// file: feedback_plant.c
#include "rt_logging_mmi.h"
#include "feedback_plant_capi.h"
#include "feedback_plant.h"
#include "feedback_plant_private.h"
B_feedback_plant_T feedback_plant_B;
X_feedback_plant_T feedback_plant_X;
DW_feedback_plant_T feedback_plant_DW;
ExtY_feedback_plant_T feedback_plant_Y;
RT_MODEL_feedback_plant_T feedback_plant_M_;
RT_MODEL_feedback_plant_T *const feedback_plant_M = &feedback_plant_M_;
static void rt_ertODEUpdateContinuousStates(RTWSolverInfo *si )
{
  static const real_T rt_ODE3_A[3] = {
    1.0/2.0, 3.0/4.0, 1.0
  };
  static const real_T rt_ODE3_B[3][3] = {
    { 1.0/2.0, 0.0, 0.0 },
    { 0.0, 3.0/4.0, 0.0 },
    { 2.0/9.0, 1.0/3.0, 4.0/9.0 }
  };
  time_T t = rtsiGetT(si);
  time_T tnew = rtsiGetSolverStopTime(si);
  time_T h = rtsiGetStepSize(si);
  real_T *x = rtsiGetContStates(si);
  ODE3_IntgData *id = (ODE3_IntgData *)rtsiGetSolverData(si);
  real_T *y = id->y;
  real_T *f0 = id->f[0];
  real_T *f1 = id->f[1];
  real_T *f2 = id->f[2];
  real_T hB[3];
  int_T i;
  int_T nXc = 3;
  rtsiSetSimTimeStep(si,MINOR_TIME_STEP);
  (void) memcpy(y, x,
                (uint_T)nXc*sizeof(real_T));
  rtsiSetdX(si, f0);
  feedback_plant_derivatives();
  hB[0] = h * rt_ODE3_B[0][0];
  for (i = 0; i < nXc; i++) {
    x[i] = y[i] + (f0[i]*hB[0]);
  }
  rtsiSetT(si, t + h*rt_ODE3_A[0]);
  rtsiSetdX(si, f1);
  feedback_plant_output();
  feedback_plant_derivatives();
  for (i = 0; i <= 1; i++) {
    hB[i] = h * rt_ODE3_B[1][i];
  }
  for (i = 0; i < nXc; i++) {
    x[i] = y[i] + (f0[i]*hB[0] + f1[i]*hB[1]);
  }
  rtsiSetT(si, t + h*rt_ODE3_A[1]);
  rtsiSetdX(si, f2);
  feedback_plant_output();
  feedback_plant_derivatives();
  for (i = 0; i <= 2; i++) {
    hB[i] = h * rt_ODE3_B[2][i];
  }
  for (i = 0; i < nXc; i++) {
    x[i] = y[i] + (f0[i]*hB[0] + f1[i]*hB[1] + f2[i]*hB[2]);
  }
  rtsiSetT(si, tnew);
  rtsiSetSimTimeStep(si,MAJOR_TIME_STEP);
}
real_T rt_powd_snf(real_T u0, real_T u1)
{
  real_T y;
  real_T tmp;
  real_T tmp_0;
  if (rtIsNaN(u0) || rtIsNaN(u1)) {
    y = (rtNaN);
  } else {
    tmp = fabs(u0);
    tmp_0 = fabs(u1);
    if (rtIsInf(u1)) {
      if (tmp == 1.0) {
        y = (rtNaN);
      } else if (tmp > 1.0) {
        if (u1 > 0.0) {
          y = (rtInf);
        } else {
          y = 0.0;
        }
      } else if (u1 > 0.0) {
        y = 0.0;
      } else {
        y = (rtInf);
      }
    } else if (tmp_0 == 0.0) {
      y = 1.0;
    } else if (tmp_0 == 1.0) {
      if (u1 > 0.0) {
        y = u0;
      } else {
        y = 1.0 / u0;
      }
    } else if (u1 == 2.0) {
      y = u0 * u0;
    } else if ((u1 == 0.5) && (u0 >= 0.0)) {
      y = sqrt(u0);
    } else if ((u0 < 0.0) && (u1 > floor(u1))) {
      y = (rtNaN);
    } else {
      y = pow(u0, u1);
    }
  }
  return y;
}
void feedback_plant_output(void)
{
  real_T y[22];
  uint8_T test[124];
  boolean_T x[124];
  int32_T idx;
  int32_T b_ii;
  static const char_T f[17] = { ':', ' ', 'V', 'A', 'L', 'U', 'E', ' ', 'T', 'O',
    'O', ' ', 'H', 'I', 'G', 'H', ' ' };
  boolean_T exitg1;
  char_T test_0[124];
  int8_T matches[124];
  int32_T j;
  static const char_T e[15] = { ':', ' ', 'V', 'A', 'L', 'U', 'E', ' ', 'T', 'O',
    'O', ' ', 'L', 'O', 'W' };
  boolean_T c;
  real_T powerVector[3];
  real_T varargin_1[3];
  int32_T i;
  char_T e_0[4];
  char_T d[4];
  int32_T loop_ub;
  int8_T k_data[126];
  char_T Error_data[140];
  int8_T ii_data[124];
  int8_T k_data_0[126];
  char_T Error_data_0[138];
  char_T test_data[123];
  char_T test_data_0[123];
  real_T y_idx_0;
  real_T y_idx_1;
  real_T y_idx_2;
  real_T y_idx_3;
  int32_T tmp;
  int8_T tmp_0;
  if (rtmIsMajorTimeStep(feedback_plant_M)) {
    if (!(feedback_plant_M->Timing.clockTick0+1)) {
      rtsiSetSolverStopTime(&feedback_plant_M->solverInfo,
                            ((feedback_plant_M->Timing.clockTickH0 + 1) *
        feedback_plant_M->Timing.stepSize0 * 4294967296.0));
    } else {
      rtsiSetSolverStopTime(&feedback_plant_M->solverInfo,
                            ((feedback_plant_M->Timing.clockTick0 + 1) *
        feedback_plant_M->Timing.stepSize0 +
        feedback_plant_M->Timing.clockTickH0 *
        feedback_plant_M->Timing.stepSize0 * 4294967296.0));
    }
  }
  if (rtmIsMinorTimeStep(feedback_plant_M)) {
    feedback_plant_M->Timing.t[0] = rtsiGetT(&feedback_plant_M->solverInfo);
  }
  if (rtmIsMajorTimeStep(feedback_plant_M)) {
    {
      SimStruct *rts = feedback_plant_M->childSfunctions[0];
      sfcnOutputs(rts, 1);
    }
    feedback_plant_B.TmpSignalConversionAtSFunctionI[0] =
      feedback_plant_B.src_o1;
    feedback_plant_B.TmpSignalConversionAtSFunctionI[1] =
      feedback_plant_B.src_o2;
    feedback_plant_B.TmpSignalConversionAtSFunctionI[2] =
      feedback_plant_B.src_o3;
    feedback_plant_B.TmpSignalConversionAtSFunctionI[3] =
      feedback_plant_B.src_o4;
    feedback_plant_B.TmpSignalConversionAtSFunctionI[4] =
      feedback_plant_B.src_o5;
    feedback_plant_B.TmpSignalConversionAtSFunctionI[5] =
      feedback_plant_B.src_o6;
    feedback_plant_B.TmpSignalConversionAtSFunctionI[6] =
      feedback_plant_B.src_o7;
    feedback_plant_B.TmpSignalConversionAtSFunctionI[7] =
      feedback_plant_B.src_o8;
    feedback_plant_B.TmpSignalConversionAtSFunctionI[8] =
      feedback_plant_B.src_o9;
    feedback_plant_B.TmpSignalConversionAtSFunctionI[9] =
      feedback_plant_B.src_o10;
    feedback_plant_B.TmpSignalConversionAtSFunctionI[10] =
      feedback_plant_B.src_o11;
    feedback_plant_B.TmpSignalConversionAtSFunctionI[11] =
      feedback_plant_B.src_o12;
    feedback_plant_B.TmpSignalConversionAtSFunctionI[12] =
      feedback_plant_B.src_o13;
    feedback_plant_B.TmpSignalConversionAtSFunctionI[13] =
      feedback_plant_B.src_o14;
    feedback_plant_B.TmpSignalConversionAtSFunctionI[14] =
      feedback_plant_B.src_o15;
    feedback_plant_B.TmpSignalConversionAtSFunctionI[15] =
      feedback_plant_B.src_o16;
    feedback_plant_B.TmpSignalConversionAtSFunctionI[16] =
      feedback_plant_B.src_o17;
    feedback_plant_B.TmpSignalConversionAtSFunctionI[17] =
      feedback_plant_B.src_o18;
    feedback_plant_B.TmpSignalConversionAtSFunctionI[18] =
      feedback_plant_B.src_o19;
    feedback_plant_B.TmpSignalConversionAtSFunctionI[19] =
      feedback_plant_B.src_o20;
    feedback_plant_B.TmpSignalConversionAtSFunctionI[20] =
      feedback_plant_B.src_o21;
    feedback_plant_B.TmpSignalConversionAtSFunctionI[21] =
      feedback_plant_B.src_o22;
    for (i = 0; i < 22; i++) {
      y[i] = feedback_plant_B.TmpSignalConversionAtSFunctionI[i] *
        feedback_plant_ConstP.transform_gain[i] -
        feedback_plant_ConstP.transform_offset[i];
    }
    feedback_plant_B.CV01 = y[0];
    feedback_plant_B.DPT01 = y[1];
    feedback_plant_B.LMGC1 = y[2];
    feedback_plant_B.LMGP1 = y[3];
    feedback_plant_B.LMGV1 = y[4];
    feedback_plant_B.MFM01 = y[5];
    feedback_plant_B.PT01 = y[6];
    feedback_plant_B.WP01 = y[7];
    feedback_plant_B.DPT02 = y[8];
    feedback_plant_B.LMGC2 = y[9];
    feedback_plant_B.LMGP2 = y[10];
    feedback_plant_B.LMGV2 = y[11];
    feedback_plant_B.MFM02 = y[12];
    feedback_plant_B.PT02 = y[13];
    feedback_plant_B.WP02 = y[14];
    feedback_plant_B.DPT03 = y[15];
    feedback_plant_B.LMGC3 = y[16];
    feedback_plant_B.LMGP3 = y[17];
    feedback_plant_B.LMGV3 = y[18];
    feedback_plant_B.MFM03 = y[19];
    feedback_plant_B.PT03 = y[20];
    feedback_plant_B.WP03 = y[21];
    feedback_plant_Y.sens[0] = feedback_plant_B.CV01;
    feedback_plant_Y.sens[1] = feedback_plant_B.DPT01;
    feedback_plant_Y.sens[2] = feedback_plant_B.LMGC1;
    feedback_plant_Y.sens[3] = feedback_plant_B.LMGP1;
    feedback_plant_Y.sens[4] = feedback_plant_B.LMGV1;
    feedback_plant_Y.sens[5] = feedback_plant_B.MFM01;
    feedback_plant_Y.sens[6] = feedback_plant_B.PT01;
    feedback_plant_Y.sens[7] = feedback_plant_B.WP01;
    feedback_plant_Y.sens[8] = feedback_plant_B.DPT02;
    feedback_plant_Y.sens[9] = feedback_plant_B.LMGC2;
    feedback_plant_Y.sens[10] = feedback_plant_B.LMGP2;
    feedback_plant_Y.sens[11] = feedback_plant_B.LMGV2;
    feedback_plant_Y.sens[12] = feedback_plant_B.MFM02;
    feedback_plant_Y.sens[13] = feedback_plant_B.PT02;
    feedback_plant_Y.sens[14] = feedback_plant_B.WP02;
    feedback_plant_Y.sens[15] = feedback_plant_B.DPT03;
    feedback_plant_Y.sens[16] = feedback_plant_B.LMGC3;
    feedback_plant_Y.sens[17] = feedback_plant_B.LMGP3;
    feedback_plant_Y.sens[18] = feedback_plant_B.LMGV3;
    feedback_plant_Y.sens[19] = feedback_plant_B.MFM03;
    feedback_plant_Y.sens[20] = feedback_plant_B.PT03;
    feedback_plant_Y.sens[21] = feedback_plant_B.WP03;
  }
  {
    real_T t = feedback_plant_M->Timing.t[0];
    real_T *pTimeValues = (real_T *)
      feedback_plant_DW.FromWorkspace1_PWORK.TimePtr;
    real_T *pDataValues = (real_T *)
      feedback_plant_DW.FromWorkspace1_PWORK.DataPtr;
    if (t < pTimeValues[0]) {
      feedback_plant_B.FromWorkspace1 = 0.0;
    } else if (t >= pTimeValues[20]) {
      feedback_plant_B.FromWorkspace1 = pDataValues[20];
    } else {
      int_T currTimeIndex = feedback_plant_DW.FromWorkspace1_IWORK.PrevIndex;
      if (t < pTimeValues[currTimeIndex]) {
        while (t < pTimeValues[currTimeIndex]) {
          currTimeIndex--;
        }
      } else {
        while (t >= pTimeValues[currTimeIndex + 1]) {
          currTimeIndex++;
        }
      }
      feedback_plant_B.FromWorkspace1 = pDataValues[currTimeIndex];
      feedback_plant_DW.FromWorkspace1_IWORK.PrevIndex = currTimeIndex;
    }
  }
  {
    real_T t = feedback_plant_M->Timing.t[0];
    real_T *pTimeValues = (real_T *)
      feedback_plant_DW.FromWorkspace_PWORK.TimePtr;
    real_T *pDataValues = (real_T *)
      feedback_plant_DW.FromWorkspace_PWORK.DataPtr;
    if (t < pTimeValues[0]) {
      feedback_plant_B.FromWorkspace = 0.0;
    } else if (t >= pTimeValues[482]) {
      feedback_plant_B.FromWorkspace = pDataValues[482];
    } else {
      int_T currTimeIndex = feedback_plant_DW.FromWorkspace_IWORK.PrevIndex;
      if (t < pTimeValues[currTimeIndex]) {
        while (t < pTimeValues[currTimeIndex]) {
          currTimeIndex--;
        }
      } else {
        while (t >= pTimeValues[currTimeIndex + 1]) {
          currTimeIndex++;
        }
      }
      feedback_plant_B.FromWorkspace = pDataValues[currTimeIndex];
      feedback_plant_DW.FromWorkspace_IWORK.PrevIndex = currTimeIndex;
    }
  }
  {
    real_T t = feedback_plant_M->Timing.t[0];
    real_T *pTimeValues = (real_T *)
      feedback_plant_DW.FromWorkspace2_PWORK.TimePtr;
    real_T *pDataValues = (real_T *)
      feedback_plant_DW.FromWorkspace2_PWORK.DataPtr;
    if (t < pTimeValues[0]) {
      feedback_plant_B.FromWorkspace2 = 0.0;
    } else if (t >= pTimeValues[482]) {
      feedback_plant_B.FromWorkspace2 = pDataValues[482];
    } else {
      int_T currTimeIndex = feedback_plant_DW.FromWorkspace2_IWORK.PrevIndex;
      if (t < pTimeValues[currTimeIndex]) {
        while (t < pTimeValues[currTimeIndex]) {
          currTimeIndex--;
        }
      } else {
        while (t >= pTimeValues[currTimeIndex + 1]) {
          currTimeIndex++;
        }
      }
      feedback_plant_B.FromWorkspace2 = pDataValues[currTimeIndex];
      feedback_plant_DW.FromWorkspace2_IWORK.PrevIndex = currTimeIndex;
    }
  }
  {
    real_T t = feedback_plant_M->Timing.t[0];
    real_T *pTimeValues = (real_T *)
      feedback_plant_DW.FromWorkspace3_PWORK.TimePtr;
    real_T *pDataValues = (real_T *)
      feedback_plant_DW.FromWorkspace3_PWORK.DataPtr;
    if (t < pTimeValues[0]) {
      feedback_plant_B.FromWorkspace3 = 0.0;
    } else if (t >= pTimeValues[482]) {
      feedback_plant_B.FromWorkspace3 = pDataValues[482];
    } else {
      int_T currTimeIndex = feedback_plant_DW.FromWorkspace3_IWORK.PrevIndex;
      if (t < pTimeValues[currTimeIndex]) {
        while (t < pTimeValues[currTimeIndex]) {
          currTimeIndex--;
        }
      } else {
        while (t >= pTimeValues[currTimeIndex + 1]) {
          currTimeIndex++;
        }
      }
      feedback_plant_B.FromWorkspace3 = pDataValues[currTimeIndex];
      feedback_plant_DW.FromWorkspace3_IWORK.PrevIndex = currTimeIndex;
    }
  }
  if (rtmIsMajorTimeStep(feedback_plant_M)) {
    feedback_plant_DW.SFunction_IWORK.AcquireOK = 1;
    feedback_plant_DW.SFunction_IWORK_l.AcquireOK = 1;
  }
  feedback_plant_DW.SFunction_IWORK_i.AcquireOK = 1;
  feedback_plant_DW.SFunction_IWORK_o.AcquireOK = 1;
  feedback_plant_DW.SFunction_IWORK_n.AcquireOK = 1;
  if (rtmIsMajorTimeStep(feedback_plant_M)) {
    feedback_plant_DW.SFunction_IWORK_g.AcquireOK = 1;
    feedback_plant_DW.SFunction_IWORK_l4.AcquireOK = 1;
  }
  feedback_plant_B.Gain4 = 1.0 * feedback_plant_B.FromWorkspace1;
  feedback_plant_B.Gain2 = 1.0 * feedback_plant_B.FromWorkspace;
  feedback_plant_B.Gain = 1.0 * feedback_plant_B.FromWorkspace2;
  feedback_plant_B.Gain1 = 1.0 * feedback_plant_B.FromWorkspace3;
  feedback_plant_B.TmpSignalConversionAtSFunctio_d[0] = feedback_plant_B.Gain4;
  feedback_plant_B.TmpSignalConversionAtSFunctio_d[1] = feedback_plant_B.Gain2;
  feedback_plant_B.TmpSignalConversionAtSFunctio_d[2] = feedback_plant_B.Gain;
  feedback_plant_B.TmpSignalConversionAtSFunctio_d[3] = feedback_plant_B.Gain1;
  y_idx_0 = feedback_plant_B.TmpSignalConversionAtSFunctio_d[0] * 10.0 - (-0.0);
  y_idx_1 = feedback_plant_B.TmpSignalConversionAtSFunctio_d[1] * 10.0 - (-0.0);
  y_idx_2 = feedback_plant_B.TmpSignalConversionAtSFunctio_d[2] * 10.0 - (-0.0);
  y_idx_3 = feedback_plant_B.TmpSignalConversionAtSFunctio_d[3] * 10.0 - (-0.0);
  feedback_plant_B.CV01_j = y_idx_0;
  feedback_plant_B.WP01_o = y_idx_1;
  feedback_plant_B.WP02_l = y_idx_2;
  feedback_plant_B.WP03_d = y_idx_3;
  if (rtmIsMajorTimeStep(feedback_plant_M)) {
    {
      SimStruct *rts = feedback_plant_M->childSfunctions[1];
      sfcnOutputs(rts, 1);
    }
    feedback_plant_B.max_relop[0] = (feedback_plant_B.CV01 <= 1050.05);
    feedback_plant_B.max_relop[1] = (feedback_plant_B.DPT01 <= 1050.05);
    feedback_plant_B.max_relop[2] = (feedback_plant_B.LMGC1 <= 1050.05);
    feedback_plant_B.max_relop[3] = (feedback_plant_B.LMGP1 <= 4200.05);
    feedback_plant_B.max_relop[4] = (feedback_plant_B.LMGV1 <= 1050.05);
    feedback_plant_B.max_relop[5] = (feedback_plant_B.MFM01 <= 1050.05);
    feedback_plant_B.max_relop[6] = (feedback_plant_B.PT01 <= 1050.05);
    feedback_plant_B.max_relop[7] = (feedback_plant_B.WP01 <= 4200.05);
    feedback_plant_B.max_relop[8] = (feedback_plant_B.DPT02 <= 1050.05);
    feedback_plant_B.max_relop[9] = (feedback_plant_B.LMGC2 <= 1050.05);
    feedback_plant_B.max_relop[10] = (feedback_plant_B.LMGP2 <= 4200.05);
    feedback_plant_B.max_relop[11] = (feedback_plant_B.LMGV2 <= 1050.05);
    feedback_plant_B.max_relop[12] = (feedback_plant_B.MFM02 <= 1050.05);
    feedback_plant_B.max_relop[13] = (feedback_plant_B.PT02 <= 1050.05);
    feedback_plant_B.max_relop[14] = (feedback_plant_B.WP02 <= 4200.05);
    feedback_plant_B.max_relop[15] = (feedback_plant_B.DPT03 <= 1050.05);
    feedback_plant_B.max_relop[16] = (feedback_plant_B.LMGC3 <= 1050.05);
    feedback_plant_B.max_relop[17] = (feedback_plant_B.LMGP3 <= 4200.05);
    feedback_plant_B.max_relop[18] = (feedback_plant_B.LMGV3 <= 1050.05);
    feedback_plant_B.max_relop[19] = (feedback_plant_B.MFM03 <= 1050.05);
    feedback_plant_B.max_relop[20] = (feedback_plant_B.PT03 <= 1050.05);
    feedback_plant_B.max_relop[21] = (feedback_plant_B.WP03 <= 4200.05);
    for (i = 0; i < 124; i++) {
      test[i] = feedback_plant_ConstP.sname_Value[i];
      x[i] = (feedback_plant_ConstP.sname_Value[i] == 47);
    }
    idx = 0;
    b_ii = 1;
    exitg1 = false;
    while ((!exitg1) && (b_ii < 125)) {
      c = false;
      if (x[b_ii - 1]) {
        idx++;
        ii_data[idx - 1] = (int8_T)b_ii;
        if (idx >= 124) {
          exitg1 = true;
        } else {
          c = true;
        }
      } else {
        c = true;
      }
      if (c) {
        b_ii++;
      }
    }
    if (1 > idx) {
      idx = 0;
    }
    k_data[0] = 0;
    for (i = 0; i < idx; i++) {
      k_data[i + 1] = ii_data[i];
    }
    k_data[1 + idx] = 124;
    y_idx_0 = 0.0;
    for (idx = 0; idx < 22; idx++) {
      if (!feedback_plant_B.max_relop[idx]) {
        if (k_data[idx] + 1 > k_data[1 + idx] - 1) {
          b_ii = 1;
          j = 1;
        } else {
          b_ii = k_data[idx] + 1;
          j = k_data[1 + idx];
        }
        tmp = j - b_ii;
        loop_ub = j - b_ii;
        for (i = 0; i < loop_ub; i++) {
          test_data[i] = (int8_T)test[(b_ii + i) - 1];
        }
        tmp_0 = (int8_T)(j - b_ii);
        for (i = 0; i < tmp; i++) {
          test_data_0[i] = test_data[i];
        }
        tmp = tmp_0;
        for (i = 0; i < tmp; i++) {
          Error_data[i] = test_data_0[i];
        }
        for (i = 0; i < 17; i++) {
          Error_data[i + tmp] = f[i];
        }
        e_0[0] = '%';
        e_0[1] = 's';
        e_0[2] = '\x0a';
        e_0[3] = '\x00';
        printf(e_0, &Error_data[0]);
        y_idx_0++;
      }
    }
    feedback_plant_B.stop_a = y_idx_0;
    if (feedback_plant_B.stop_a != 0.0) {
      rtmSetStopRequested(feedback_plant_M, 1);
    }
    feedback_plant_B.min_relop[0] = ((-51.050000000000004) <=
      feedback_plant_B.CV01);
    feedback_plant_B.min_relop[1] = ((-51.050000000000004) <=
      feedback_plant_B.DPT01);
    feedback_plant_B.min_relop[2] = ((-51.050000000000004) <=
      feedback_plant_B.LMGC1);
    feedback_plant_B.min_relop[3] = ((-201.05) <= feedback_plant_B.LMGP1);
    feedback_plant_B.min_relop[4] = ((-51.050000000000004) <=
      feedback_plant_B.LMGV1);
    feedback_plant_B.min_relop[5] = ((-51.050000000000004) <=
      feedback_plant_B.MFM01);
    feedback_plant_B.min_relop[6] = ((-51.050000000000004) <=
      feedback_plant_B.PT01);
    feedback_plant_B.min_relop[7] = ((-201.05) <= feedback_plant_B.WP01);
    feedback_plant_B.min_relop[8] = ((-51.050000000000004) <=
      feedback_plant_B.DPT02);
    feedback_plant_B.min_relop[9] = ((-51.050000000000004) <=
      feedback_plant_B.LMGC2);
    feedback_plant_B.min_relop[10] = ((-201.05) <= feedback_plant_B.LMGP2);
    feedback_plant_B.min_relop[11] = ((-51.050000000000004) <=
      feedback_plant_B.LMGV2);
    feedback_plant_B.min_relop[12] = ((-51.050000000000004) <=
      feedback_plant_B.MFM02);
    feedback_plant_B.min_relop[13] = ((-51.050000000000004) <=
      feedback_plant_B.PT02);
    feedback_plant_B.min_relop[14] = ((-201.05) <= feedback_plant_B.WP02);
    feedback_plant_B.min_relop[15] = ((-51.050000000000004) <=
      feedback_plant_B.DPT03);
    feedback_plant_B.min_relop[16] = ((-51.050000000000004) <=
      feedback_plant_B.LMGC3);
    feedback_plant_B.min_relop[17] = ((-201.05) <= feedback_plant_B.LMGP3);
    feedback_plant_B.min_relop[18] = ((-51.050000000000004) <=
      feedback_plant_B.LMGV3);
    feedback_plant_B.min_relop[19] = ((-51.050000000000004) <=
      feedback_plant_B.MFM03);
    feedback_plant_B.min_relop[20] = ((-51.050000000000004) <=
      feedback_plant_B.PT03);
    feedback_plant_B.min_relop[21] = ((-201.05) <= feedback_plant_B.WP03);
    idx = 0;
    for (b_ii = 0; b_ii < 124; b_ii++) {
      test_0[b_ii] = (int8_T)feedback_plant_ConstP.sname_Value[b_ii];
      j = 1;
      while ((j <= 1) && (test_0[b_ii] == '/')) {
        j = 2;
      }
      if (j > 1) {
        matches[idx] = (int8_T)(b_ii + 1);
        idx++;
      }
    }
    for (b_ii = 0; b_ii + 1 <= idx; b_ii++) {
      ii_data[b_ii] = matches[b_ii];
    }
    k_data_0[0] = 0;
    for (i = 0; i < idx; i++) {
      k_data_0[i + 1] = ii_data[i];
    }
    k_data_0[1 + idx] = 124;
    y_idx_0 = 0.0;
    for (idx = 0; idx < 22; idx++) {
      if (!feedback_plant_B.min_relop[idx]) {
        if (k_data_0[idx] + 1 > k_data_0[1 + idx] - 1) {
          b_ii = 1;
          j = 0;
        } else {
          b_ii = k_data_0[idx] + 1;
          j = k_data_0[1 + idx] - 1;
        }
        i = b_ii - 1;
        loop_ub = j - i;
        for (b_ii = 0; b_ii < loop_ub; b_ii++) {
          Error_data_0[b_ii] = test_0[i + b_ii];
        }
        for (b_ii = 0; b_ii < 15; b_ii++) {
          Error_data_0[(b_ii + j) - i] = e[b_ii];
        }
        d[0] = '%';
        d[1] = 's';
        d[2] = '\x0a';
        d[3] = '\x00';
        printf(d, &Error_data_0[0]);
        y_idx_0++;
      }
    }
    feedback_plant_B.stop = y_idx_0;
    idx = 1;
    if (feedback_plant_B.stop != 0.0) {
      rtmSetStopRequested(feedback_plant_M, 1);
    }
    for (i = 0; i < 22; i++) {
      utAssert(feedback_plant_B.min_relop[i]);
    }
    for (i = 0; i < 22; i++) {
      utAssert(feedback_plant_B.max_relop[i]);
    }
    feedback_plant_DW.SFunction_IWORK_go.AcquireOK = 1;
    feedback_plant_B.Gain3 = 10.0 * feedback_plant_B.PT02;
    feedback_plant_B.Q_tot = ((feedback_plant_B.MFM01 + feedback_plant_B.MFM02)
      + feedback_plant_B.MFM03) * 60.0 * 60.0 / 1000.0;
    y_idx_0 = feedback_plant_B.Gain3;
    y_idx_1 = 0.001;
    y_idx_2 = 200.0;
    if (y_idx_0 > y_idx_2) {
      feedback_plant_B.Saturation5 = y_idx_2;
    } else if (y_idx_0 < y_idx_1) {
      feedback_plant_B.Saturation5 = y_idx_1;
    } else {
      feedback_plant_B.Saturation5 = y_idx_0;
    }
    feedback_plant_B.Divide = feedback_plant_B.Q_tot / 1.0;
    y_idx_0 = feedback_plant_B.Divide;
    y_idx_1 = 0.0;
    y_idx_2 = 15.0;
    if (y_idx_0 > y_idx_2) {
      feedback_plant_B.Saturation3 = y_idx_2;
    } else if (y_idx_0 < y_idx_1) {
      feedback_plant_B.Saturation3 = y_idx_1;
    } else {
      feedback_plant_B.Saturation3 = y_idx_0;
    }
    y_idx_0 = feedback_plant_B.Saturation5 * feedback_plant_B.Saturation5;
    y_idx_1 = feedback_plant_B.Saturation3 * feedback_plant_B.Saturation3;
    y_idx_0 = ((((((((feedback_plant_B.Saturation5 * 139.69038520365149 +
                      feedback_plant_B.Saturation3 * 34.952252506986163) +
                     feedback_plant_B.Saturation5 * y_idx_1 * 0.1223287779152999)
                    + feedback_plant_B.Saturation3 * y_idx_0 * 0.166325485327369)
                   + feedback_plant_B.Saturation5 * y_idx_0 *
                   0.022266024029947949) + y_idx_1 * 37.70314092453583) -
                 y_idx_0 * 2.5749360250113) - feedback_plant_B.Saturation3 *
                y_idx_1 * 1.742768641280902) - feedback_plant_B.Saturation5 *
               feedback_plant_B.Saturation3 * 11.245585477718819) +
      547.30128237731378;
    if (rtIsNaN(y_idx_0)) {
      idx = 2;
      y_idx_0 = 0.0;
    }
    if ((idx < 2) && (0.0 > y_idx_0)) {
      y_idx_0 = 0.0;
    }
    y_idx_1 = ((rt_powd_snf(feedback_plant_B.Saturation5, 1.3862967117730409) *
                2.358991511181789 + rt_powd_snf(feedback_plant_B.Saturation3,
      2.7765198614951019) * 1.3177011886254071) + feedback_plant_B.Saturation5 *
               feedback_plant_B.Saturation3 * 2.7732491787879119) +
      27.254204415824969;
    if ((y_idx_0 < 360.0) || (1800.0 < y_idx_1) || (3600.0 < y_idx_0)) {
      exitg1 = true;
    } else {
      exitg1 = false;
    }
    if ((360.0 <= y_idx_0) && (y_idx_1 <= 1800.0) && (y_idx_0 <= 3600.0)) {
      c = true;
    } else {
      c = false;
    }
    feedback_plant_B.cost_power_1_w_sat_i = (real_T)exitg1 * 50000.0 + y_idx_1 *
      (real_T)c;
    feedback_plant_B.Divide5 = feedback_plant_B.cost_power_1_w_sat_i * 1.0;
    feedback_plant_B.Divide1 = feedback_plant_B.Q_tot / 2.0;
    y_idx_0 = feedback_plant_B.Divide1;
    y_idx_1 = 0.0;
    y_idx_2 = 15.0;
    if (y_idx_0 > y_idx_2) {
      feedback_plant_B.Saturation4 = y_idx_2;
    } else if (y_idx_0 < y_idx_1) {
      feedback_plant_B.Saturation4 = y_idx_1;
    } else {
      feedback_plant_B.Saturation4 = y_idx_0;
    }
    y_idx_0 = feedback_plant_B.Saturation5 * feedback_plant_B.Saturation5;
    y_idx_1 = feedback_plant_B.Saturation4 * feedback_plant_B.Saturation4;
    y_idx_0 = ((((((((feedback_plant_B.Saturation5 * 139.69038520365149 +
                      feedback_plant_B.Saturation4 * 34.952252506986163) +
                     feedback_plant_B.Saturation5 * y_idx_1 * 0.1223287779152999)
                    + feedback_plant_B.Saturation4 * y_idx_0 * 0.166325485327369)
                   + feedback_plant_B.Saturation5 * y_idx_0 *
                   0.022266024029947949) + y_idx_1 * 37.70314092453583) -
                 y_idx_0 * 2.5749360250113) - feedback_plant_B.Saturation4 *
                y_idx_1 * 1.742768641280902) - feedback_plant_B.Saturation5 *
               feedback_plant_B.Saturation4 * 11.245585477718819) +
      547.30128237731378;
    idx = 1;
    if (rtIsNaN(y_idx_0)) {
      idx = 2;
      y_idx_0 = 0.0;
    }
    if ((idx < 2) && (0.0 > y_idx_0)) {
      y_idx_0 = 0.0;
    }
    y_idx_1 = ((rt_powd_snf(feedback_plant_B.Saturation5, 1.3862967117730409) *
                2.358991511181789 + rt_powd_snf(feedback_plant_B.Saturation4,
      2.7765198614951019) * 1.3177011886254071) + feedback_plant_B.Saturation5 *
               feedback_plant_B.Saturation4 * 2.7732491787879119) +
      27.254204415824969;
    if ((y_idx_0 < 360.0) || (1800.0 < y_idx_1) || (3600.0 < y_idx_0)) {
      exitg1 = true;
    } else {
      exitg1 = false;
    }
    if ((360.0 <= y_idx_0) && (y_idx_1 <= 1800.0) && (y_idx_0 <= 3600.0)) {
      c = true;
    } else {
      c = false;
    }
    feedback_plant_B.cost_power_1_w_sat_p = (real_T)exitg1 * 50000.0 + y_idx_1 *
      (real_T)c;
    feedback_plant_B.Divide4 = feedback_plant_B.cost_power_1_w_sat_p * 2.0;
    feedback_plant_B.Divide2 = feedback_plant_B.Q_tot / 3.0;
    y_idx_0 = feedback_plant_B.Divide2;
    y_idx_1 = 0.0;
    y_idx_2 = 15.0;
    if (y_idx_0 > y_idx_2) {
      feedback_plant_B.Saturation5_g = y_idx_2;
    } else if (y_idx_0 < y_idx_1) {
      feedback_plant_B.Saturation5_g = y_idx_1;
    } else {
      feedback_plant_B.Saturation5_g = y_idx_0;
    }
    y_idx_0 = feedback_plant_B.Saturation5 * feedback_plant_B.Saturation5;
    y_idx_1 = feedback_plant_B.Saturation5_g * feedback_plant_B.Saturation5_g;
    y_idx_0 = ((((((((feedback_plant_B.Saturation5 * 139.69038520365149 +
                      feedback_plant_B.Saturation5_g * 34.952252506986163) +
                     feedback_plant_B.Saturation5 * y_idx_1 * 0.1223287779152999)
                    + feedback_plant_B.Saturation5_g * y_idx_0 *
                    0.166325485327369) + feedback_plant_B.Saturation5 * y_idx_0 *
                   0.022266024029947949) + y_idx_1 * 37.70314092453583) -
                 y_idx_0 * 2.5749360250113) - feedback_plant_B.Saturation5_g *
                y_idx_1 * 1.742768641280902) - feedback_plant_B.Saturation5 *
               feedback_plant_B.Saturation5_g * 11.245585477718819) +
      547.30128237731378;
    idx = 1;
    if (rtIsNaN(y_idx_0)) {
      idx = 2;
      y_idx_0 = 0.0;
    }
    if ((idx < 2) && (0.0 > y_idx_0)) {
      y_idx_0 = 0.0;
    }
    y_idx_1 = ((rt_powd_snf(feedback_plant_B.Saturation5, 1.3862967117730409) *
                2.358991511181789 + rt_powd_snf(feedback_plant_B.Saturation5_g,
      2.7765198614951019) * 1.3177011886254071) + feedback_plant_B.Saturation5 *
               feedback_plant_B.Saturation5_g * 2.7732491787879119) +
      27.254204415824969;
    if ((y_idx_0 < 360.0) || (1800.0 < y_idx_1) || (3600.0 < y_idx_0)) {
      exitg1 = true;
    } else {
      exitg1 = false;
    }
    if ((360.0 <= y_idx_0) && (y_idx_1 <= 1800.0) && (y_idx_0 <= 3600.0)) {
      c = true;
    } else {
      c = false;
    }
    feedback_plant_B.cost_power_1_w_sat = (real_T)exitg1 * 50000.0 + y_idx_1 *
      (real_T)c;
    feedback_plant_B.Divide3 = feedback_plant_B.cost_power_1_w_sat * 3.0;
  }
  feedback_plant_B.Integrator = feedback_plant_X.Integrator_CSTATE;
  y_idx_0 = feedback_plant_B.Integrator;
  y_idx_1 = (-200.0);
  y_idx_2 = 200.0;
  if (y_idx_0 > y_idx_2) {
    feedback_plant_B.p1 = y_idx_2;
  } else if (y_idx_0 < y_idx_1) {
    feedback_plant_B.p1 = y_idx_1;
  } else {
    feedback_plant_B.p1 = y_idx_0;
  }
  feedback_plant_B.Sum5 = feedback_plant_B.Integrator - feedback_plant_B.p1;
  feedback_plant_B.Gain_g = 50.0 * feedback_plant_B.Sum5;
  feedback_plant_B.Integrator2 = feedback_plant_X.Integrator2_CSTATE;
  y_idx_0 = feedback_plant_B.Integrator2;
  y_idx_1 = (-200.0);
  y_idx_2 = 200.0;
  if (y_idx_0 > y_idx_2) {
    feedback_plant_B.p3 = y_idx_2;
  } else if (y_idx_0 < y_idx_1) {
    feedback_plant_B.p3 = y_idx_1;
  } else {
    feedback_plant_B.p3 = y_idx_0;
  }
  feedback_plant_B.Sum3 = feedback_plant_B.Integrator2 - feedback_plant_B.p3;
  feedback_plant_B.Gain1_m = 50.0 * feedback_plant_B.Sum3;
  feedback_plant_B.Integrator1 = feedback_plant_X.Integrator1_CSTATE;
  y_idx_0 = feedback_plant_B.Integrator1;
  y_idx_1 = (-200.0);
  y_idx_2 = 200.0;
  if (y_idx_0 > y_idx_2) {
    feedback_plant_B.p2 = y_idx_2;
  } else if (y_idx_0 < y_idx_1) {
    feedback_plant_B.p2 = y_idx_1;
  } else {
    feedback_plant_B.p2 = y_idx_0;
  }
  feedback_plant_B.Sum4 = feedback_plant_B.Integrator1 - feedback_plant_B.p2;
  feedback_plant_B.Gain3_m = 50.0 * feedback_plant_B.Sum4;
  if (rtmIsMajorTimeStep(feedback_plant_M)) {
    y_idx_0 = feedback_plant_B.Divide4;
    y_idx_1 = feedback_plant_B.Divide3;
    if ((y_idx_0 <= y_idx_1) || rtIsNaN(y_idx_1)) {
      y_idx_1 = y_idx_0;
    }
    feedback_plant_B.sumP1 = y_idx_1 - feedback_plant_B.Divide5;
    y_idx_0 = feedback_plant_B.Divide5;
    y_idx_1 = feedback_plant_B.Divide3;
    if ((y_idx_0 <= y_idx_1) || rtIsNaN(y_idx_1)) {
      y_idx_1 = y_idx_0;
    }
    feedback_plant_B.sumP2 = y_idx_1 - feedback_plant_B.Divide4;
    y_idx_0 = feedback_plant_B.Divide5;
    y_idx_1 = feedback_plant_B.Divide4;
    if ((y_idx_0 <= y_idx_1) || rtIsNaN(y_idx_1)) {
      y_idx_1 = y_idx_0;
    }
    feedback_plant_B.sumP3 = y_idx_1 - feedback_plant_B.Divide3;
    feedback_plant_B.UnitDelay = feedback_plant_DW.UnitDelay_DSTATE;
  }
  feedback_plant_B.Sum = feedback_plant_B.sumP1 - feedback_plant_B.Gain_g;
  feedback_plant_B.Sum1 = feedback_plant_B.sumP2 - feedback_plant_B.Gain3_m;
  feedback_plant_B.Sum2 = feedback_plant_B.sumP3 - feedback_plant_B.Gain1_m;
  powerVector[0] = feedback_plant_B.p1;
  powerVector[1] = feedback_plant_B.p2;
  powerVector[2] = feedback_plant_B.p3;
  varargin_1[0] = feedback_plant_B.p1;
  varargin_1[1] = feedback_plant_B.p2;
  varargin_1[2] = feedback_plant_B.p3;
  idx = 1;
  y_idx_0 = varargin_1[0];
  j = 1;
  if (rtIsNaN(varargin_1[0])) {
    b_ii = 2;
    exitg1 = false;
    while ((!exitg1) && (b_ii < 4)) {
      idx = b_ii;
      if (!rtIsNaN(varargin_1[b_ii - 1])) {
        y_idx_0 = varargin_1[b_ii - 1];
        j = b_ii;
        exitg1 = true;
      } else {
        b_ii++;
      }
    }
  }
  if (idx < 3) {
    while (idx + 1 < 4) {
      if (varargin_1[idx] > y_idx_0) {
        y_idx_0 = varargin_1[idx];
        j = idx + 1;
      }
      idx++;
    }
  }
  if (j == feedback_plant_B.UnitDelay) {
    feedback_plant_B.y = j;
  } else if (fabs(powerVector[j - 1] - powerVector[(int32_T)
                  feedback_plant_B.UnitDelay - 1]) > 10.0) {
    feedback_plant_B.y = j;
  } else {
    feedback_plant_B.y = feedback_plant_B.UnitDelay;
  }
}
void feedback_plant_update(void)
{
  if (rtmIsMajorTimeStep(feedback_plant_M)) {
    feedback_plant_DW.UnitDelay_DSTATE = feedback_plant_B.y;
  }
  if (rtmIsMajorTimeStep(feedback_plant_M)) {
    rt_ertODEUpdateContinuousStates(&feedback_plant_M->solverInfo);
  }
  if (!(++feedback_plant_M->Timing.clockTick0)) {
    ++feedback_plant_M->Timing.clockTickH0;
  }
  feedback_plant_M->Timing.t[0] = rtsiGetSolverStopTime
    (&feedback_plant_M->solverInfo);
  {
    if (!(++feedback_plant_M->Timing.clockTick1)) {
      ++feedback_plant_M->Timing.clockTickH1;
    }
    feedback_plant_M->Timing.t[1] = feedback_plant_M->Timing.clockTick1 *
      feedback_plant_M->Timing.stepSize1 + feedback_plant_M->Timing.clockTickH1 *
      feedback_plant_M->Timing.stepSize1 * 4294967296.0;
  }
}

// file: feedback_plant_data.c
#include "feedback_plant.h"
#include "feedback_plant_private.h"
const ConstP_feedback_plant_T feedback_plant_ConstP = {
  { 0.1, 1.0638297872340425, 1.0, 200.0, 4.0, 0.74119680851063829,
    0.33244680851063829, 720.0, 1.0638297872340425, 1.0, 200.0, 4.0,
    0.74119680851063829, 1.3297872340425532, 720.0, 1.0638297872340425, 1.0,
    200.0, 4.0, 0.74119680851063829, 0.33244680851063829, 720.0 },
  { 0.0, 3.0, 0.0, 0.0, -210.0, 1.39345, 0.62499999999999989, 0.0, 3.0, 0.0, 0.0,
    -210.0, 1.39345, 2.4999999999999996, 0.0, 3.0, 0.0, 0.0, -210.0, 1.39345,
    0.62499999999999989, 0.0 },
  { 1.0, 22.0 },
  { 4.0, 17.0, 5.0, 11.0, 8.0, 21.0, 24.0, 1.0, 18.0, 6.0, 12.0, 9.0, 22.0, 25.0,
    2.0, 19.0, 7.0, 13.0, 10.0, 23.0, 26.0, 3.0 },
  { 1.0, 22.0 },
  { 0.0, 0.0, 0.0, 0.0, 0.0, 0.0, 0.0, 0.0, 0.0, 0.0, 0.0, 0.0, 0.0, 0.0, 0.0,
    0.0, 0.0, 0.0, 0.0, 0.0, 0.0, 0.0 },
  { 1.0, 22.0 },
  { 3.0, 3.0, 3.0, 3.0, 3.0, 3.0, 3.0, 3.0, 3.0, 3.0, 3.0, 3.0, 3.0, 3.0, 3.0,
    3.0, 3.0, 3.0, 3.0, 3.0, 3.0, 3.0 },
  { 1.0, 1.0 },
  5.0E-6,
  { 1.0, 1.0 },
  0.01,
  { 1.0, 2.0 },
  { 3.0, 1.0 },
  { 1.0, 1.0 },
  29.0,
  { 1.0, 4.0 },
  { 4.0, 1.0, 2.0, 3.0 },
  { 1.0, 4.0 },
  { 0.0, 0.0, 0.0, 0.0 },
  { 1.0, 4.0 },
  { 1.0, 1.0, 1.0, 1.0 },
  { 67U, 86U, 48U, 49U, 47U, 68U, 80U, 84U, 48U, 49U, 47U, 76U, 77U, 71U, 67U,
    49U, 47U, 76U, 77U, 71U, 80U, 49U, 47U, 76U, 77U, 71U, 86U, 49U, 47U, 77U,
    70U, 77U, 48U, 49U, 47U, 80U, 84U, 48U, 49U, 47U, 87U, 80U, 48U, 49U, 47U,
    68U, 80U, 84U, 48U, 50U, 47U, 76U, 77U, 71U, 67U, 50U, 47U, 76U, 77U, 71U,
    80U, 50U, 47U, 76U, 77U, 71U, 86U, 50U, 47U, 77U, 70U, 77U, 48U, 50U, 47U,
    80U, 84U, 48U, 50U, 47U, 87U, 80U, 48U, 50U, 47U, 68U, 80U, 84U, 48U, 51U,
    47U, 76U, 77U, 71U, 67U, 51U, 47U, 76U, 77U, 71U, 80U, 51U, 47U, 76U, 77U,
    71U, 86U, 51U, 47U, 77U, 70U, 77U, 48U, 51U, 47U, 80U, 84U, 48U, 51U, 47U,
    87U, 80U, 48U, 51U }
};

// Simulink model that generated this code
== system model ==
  sens : Outport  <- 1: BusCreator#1
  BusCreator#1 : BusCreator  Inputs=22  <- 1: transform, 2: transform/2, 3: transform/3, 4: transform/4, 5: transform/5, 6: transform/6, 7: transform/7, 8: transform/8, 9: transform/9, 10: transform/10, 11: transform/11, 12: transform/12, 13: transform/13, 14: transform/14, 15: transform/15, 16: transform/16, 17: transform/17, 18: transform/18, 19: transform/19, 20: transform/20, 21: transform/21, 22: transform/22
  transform : MATLAB Function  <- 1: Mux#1
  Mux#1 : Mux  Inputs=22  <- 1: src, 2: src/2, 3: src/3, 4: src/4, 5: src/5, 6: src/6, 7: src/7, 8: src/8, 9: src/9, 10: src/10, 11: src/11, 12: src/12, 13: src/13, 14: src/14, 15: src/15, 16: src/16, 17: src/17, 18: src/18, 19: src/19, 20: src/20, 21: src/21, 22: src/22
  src : xpcnilib/A//D/M Series/PCI-6229 AD
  PCI6229DA#1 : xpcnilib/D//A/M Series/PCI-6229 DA  <- 1: MATLABFunction#1, 2: MATLABFunction#1/2, 3: MATLABFunction#1/3, 4: MATLABFunction#1/4
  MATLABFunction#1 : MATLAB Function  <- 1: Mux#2, 2: gain, 3: offset
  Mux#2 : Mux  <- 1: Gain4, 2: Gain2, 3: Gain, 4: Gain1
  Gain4 : Gain  <- 1: FromWorkspace1
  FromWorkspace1 : FromWorkspace
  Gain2 : Gain  <- 1: FromWorkspace
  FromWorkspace : FromWorkspace
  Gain : Gain  <- 1: FromWorkspace2
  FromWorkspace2 : FromWorkspace
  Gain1 : Gain  <- 1: FromWorkspace3
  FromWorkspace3 : FromWorkspace
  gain : Constant  Value=gain
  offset : Constant  Value=offset
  stop : Stop  <- 1: MATLABFunction#2
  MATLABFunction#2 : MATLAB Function  <- 1: CheckStaticUpperBound#1, 2: sname
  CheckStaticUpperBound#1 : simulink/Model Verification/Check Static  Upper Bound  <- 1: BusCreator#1
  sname : Constant  Value=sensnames
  Stop#1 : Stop  <- 1: MATLABFunction#3
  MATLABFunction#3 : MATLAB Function  <- 1: CheckStaticLowerBound#1, 2: sname
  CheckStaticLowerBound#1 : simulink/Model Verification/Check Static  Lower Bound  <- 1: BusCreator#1
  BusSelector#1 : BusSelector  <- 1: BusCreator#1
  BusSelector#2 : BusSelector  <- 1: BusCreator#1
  Gain#1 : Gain  Gain=50  <- 1: Sum5
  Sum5 : Sum  Inputs=+-  <- 1: Integrator, 2: Saturate#1
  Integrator : Integrator  UpperSaturationLimit=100  LowerSaturationLimit=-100  <- 1: Sum
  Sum : Sum  Inputs=+-  <- 1: test, 2: Gain#1
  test : MATLAB Function  <- 1: Divide5, 2: Divide4, 3: Divide3
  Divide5 : Product  Inputs=**  <- 1: cost_power_1, 2: Constant#1
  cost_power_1 : MATLAB Function  <- 1: Saturation5, 2: Saturation3
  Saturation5 : Saturate  UpperLimit=200  LowerLimit=0.001  <- 1: Gain3
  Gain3 : Gain  Gain=10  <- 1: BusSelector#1
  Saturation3 : Saturate  UpperLimit=15  LowerLimit=0  <- 1: Divide
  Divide : Product  Inputs=*/  <- 1: MATLABFunction#4, 2: Constant#1
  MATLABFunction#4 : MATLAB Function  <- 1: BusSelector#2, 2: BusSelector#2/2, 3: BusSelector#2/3
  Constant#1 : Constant
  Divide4 : Product  Inputs=**  <- 1: MATLABFunction#5, 2: Constant#2
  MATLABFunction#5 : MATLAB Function  <- 1: Saturation5, 2: Saturation4
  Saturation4 : Saturate  UpperLimit=15  LowerLimit=0  <- 1: Divide1
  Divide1 : Product  Inputs=*/  <- 1: MATLABFunction#4, 2: Constant#2
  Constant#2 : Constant  Value=2
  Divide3 : Product  Inputs=**  <- 1: MATLABFunction#6, 2: Constant#3
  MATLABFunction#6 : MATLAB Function  <- 1: Saturation5, 2: Saturate#2
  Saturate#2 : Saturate  UpperLimit=15  LowerLimit=0  <- 1: Divide2
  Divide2 : Product  Inputs=*/  <- 1: MATLABFunction#4, 2: Constant#3
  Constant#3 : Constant  Value=3
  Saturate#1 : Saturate  UpperLimit=200  LowerLimit=-200  <- 1: Integrator
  Gain#2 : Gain  Gain=50  <- 1: Sum3
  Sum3 : Sum  Inputs=+-  <- 1: Integrator2, 2: Saturate#3
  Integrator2 : Integrator  UpperSaturationLimit=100  LowerSaturationLimit=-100  <- 1: Sum2
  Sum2 : Sum  Inputs=+-  <- 1: test/3, 2: Gain#2
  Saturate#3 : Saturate  UpperLimit=200  LowerLimit=-200  <- 1: Integrator2
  Gain#3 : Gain  Gain=50  <- 1: Sum4
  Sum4 : Sum  Inputs=+-  <- 1: Integrator1, 2: Saturate#4
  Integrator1 : Integrator  UpperSaturationLimit=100  LowerSaturationLimit=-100  <- 1: Sum1
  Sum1 : Sum  Inputs=+-  <- 1: test/2, 2: Gain#3
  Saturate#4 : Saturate  UpperLimit=200  LowerLimit=-200  <- 1: Integrator1
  UnitDelay : UnitDelay  InitialCondition=1  <- 1: MATLABFunction#7
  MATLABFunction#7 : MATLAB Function  <- 1: UnitDelay, 2: Saturate#1, 3: Saturate#4, 4: Saturate#3
== matlab function transform ==
function [CV01,WP01,WP02,WP03]  = fcn(u,gain,offset)
   y = u.*gain-offset;
CV01 = y(1);
WP01 = y(2);
WP02 = y(3);
WP03 = y(4);

== matlab function transform ==
function [CV01,DPT01,LMGC1,LMGP1,LMGV1,MFM01,PT01,WP01,DPT02,LMGC2,LMGP2,LMGV2,MFM02,PT02,WP02,DPT03,LMGC3,LMGP3,LMGV3,MFM03,PT03,WP03]  = fcn(u,gain,offset)
   y = u(:).*gain(:)-offset(:);
CV01 = y(1);
DPT01 = y(2);
LMGC1 = y(3);
LMGP1 = y(4);
LMGV1 = y(5);
MFM01 = y(6);
PT01 = y(7);
WP01 = y(8);
DPT02 = y(9);
LMGC2 = y(10);
LMGP2 = y(11);
LMGV2 = y(12);
MFM02 = y(13);
PT02 = y(14);
WP02 = y(15);
DPT03 = y(16);
LMGC3 = y(17);
LMGP3 = y(18);
LMGV3 = y(19);
MFM03 = y(20);
PT03 = y(21);
WP03 = y(22);

== matlab function MATLABFunction#4 ==
function Q_tot = fcn(Q1, Q2, Q3)

Q_tot = ((Q1 + Q2 + Q3) *60 * 60)/1000;

== matlab function MATLABFunction#2 ==
function stop  = fcn(chk, sensnames)
%#codegen
%test = char(sensnames.');
test = sensnames.';
k = find(test == 47);
k = [0 k];
k = [k numel(test)];
stop = 0;
for i = 1:numel(chk)
    if chk(i) == 0
        str = char(test(k(i)+1:k(i+1)-1));
        Error = [str ': VALUE TOO HIGH ']
        coder.ceval('printf', ['%s' 10 0], Error);
        stop = stop+1;
    end
end

== matlab function MATLABFunction#3 ==
function stop  = fcn(chk, sensnames)
%#codegen
test = char(sensnames.');
k = strfind(test, '/');
k = [0 k];
k = [k numel(sensnames)];
stop = 0;
for i = 1:numel(chk)
    if chk(i) == 0
        str = char(test(k(i)+1:k(i+1)-1));
        Error = [str ': VALUE TOO LOW']
        coder.ceval('printf', ['%s' 10 0], Error);
        stop = stop+1;
    end
end

== matlab function cost_power_1 ==
function cost_power_1_w_sat = cost_power_1(H,Q)
%#codegen

%    This function was generated by the Symbolic Math Toolbox version 7.0.
%    14-Oct-2016 11:25:59

t2 = H.^2;
t3 = Q.^2;
t4 = H.*1.396903852036515e2;
t5 = Q.*3.495225250698616e1;
t6 = H.*t3.*1.223287779152999e-1;
t7 = Q.*t2.*1.66325485327369e-1;
t8 = H.*t2.*2.226602402994795e-2;
t9 = t3.*3.770314092453583e1;
t13 = t2.*2.5749360250113;
t14 = Q.*t3.*1.742768641280902;
t15 = H.*Q.*1.124558547771882e1;
t10 = t4+t5+t6+t7+t8+t9-t13-t14-t15+5.473012823773138e2;
t11 = t10;
t12 = max([t11,0.0]);
t16 = H.^1.386296711773041;
t17 = t16.*2.358991511181789;
t18 = Q.^2.776519861495102;
t19 = t18.*1.317701188625407;
t20 = H.*Q.*2.773249178787912;
t21 = t17+t19+t20+2.725420441582497e1;
cost_power_1_w_sat = double(((t12 < 3.6e2) || (1.8e3 < t21)) || (3.6e3 < t12)).*5.0e4+t21.*double(((3.6e2 <= t12) && (t21 <= 1.8e3)) && (t12 <= 3.6e3));

== matlab function MATLABFunction#5 ==
function cost_power_1_w_sat = cost_power_2(H,Q)
%#codegen

%    This function was generated by the Symbolic Math Toolbox version 7.0.
%    14-Oct-2016 11:25:59

t2 = H.^2;
t3 = Q.^2;
t4 = H.*1.396903852036515e2;
t5 = Q.*3.495225250698616e1;
t6 = H.*t3.*1.223287779152999e-1;
t7 = Q.*t2.*1.66325485327369e-1;
t8 = H.*t2.*2.226602402994795e-2;
t9 = t3.*3.770314092453583e1;
t13 = t2.*2.5749360250113;
t14 = Q.*t3.*1.742768641280902;
t15 = H.*Q.*1.124558547771882e1;
t10 = t4+t5+t6+t7+t8+t9-t13-t14-t15+5.473012823773138e2;
t11 = t10;
t12 = max([t11,0.0]);
t16 = H.^1.386296711773041;
t17 = t16.*2.358991511181789;
t18 = Q.^2.776519861495102;
t19 = t18.*1.317701188625407;
t20 = H.*Q.*2.773249178787912;
t21 = t17+t19+t20+2.725420441582497e1;
cost_power_1_w_sat = double(((t12 < 3.6e2) || (1.8e3 < t21)) || (3.6e3 < t12)).*5.0e4+t21.*double(((3.6e2 <= t12) && (t21 <= 1.8e3)) && (t12 <= 3.6e3));

== matlab function MATLABFunction#6 ==
function cost_power_1_w_sat = cost_power_3(H,Q)
%#codegen

%    This function was generated by the Symbolic Math Toolbox version 7.0.
%    14-Oct-2016 11:25:59

t2 = H.^2;
t3 = Q.^2;
t4 = H.*1.396903852036515e2;
t5 = Q.*3.495225250698616e1;
t6 = H.*t3.*1.223287779152999e-1;
t7 = Q.*t2.*1.66325485327369e-1;
t8 = H.*t2.*2.226602402994795e-2;
t9 = t3.*3.770314092453583e1;
t13 = t2.*2.5749360250113;
t14 = Q.*t3.*1.742768641280902;
t15 = H.*Q.*1.124558547771882e1;
t10 = t4+t5+t6+t7+t8+t9-t13-t14-t15+5.473012823773138e2;
t11 = t10;
t12 = max([t11,0.0]);
t16 = H.^1.386296711773041;
t17 = t16.*2.358991511181789;
t18 = Q.^2.776519861495102;
t19 = t18.*1.317701188625407;
t20 = H.*Q.*2.773249178787912;
t21 = t17+t19+t20+2.725420441582497e1;
cost_power_1_w_sat = double(((t12 < 3.6e2) || (1.8e3 < t21)) || (3.6e3 < t12)).*5.0e4+t21.*double(((3.6e2 <= t12) && (t21 <= 1.8e3)) && (t12 <= 3.6e3));
